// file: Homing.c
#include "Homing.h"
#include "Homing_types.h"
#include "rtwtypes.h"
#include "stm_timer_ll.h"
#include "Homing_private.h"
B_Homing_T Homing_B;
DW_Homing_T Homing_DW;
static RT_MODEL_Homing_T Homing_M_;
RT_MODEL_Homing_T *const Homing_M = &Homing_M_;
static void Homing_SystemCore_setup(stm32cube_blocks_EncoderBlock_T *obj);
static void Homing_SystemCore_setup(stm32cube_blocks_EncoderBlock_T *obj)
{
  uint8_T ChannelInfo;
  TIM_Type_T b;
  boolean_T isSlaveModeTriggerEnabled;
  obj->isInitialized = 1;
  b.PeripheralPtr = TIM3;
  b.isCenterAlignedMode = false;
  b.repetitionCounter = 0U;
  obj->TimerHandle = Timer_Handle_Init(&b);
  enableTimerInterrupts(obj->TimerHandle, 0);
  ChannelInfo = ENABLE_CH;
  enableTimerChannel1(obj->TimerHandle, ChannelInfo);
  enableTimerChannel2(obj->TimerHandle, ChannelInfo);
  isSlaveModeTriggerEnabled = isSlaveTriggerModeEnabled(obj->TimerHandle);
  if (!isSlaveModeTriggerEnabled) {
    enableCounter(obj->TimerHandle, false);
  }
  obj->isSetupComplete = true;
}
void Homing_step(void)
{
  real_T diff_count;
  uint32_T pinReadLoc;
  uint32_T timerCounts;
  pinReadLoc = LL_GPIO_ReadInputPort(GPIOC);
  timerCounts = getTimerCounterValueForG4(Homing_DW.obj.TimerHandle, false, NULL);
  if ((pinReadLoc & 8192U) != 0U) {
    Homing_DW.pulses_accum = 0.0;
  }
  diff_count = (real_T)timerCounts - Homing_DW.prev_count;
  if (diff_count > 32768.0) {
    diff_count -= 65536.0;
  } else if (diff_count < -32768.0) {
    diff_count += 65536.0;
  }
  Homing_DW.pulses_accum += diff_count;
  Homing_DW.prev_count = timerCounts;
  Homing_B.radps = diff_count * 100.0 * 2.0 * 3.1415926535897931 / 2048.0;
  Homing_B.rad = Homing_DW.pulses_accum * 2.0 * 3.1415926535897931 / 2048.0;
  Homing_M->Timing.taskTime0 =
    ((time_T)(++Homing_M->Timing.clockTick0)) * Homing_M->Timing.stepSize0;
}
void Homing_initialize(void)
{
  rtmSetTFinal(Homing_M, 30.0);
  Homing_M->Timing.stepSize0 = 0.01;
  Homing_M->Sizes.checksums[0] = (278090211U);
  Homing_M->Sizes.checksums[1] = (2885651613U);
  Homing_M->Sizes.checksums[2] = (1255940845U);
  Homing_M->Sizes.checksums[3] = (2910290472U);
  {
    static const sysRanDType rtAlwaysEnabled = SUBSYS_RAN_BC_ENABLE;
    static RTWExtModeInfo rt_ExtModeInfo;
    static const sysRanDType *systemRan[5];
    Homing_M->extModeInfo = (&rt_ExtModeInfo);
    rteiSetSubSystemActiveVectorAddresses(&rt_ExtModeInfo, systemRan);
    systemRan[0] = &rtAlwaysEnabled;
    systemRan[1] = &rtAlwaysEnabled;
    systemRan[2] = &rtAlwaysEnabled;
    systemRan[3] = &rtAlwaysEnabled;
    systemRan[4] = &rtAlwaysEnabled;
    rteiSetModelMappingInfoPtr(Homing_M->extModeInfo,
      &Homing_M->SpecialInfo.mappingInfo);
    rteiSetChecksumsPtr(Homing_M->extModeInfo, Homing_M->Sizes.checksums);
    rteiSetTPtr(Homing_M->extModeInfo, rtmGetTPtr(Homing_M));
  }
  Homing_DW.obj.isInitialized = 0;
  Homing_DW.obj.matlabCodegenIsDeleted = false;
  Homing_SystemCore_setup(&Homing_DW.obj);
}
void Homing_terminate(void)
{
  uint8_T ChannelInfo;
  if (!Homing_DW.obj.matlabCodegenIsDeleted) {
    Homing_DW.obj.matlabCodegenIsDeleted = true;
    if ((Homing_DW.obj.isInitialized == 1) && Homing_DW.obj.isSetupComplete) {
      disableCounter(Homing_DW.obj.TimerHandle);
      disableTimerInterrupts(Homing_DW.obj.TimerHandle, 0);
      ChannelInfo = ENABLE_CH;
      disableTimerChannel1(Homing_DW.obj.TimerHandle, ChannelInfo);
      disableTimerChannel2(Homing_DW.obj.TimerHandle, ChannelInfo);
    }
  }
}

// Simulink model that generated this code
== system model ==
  MATLABFunction#1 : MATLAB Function  <- 1: MATLABFunction#2, 2: MATLABFunction#2/2, 3: Constant#1
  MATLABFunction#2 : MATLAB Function  <- 1: DigitalPortRead#1, 2: DataTypeConversion#1, 3: Constant#1, 4: Constant#2
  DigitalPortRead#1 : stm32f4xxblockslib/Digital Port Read
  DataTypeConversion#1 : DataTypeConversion  <- 1: Encoder#1
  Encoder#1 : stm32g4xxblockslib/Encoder
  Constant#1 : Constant  Value=2048
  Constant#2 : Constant  Value=100
== matlab function MATLABFunction#2 ==
function [pps, pulses] = qei_x4(reset, count, ppr, freq)
enc_period = 65536 - mod(65536,ppr*4);
persistent prev_count
persistent pulses_accum
persistent diff_count

if isempty(prev_count)
    prev_count = 0;
end

if isempty(pulses_accum)
    pulses_accum = 0;
end

if isempty(diff_count)
    diff_count = 0;
end

if reset == 1
    pulses_accum = 0
end

diff_count = count - prev_count;

if diff_count > enc_period / 2
    diff_count = diff_count - enc_period;
elseif diff_count < -enc_period / 2
    diff_count = diff_count + enc_period;
end

pulses_accum = pulses_accum + diff_count;

pulses = pulses_accum;
pps = double(diff_count)*freq;

prev_count = count;
end

== matlab function MATLABFunction#1 ==
function [radps, rad] = to_SI_unit(vel, pos, ppr)
    radps = (vel * 2 * pi) / ppr;

    rad = (pos * 2 * pi) / ppr;
end
